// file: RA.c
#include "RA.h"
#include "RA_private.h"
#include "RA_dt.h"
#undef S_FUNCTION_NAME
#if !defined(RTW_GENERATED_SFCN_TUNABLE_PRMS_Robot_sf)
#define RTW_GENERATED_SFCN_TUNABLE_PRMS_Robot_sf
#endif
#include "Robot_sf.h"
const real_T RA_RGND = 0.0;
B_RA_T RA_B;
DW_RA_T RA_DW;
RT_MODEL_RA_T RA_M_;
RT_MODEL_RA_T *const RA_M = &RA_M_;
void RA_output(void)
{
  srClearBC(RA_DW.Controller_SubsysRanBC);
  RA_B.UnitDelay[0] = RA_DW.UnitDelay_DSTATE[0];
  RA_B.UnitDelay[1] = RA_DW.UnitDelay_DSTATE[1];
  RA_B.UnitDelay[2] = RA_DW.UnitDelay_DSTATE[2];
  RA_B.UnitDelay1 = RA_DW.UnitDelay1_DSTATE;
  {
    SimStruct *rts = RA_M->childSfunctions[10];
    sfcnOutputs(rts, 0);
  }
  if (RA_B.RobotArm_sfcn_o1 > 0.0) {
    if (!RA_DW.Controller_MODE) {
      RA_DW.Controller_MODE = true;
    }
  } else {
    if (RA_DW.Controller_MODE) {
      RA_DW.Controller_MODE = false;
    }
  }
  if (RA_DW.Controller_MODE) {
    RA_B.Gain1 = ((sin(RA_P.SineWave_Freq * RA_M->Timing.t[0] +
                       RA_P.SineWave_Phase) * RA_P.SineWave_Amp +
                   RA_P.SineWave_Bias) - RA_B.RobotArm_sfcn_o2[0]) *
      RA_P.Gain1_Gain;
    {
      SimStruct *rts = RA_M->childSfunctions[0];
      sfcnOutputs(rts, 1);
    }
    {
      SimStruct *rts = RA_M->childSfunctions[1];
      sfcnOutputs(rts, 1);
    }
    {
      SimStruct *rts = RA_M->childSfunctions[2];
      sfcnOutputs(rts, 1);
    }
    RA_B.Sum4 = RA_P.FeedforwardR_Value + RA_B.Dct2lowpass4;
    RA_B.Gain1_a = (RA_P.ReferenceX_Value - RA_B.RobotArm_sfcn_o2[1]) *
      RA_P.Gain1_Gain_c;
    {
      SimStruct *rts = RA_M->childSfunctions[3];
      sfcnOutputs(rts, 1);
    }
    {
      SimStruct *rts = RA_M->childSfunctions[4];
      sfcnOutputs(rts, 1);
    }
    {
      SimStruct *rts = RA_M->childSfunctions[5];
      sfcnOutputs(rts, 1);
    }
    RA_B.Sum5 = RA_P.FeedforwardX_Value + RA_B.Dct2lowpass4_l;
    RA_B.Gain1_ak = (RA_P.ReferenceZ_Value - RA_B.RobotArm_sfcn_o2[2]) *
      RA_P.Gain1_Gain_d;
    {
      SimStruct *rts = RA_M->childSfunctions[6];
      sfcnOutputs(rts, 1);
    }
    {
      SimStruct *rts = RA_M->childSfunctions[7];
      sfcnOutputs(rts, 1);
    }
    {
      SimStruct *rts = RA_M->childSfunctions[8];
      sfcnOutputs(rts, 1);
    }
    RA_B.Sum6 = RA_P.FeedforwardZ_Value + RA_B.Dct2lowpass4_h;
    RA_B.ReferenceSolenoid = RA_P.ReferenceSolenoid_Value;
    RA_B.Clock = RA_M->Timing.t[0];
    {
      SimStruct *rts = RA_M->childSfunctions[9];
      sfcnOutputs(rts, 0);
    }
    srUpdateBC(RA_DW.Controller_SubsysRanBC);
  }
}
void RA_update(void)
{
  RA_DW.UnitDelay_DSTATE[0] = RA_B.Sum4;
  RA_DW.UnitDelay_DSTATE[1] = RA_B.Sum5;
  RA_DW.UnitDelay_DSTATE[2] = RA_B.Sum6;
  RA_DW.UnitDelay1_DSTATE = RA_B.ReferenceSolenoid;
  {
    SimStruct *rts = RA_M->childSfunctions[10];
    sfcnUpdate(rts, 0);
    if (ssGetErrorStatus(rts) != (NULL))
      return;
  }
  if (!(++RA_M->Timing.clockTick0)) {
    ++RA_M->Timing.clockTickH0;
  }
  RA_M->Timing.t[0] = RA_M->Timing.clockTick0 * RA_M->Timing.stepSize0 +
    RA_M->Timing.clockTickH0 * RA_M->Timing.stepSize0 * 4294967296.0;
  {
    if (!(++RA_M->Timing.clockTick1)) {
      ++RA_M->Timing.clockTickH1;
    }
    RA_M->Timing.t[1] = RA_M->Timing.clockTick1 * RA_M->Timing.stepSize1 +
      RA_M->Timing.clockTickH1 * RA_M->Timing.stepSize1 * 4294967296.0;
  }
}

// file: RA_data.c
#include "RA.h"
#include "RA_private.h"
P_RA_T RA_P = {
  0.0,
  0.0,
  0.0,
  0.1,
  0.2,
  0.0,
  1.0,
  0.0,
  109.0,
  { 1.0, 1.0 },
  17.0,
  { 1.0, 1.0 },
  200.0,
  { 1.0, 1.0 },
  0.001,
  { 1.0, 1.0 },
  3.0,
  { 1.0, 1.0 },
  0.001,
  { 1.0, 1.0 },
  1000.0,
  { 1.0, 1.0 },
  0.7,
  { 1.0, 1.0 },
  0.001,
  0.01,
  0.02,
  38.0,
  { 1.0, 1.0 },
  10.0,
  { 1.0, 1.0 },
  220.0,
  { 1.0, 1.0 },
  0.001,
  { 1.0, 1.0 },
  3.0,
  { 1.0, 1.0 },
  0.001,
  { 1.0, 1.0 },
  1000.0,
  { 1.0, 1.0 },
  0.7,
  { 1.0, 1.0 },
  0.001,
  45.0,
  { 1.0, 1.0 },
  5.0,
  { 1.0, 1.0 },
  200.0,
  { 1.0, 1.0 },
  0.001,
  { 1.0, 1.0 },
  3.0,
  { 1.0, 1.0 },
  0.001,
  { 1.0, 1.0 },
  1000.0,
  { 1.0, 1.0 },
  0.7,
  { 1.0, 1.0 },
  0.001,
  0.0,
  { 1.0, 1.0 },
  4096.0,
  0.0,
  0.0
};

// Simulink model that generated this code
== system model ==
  UnitDelay : UnitDelay  <- 1: Controller
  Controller : Subsystem  <- 1: RobotArm_sfcn/2, Enable: RobotArm_sfcn
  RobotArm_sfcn : S-Function  FunctionName=Robot_sf  <- 1: UnitDelay, 2: UnitDelay1
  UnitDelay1 : UnitDelay  <- 1: Controller/2
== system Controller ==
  Inport#1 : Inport
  EnablePort#1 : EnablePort
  Outport#1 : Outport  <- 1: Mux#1
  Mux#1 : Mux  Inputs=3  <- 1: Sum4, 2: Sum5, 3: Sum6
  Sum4 : Sum  Inputs=++  <- 1: FeedforwardR, 2: Dct2lowpass4
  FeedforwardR : Constant  Value=0
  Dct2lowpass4 : S-Function  FunctionName=dlowpass2  <- 1: SFunction#1
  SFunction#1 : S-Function  FunctionName=dweakint  <- 1: SFunction#2
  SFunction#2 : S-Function  FunctionName=dleadlag  <- 1: Gain1
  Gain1 : Gain  Gain=109  <- 1: Sum#1
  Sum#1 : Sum  Inputs=+-  <- 1: SineWave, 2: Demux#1
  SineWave : Sin  Amplitude=.2
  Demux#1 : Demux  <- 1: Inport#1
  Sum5 : Sum  Inputs=++  <- 1: FeedforwardX, 2: SFunction#3
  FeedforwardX : Constant  Value=0
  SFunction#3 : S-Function  FunctionName=dlowpass2  <- 1: SFunction#4
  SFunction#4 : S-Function  FunctionName=dweakint  <- 1: SFunction#5
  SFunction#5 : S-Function  FunctionName=dleadlag  <- 1: Gain#1
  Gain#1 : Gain  Gain=38  <- 1: Sum#2
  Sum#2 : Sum  Inputs=+-  <- 1: ReferenceX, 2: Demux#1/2
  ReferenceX : Constant  Value=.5
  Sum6 : Sum  Inputs=++  <- 1: FeedforwardZ, 2: SFunction#6
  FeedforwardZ : Constant  Value=0.1
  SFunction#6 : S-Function  FunctionName=dlowpass2  <- 1: SFunction#7
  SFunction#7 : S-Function  FunctionName=dweakint  <- 1: SFunction#8
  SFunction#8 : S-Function  FunctionName=dleadlag  <- 1: Gain#2
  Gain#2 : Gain  Gain=45  <- 1: Sum#3
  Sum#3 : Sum  Inputs=+-  <- 1: ReferenceZ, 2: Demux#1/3
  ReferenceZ : Constant
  Outport#2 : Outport  InitialOutput=0  <- 1: ReferenceSolenoid
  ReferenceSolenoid : Constant  Value=0
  Clock : Clock
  SFunction#9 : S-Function  FunctionName=sf_rt_scope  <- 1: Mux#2
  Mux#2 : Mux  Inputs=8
